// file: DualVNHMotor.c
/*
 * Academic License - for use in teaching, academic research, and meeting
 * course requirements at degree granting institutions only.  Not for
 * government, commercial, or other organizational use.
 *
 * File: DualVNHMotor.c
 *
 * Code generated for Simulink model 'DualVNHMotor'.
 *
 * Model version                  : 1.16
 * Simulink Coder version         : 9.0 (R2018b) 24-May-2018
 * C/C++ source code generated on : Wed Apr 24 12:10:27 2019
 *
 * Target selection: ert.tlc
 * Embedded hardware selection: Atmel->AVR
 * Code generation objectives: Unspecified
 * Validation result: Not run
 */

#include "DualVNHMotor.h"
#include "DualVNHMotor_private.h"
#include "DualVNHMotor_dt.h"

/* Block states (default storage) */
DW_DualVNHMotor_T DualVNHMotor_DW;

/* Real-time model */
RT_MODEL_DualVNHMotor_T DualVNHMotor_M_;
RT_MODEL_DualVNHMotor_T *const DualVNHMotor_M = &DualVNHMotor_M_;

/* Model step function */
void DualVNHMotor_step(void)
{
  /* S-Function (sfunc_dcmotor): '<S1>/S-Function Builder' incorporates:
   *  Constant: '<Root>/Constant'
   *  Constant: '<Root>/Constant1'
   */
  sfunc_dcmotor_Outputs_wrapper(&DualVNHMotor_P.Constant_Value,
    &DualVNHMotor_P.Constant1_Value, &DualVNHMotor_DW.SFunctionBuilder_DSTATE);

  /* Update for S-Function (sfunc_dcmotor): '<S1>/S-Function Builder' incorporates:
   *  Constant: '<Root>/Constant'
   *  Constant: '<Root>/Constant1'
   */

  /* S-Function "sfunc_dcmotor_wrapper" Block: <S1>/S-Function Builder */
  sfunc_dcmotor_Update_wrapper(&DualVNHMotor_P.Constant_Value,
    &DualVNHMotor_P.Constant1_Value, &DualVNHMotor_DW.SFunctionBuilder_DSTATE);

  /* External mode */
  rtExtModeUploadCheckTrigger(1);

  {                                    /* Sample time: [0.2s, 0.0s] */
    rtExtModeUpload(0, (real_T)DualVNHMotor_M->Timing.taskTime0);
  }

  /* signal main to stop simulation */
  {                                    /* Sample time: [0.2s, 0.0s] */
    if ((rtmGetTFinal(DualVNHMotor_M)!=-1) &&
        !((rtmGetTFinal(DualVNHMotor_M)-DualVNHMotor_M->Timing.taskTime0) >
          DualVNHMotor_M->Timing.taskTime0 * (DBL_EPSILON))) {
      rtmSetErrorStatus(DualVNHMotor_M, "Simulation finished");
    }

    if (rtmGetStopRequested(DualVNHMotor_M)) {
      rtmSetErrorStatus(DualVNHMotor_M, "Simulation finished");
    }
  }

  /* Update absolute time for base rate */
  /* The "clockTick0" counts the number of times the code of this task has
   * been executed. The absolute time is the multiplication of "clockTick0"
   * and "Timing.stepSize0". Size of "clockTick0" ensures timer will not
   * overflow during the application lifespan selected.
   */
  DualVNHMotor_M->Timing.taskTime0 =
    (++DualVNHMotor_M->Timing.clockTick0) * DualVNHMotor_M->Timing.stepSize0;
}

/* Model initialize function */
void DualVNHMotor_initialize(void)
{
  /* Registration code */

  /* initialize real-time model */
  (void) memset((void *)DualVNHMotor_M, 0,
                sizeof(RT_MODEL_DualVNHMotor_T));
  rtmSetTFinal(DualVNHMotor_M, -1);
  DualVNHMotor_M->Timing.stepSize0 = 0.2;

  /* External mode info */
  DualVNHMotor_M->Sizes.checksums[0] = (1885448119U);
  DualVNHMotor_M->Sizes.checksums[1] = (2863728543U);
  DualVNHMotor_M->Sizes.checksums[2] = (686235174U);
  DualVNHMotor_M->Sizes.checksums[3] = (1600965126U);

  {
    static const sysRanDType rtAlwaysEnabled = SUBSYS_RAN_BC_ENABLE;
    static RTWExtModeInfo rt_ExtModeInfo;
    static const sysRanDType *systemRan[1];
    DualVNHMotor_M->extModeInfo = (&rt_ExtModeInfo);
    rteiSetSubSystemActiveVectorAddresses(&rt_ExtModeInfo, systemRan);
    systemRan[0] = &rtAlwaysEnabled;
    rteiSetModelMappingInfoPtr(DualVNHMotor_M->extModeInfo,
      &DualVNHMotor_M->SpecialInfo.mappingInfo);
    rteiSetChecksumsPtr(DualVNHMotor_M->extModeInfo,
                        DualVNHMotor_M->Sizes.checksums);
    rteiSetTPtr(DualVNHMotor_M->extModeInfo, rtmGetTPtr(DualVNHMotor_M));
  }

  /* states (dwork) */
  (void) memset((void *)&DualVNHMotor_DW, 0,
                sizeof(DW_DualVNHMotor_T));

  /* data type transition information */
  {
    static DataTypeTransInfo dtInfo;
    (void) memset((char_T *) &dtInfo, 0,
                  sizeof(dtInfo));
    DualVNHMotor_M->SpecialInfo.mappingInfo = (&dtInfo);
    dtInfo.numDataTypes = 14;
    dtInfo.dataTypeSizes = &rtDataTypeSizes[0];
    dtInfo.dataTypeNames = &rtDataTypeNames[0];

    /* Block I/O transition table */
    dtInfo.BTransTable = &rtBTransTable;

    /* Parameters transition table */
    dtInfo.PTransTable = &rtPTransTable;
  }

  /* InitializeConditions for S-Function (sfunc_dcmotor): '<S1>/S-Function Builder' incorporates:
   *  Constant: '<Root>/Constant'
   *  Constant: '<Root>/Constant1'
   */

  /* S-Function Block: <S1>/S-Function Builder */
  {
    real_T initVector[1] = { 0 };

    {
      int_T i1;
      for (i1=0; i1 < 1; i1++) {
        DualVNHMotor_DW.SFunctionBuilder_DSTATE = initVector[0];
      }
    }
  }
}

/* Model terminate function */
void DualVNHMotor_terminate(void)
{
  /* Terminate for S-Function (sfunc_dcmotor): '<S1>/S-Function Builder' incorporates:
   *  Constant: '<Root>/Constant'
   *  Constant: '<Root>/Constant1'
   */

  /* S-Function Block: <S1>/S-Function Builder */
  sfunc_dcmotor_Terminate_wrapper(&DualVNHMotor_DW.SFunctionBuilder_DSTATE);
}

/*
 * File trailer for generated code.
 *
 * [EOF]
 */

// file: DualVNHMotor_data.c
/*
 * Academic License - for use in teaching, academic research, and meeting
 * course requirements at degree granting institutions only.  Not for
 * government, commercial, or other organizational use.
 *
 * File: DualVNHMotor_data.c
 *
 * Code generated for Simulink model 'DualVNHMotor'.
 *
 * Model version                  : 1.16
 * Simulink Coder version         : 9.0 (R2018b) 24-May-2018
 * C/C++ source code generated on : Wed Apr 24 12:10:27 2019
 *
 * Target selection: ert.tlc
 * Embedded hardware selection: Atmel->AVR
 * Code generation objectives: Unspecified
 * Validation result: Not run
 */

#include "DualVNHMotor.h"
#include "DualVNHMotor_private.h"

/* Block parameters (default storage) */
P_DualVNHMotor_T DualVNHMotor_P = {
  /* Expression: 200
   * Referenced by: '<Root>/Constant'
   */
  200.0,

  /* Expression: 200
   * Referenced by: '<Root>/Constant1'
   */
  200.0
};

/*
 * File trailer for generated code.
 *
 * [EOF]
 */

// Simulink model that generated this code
simulink model "DualVNHMotor"  (R2018b)
settings: Solver=FixedStepAuto  StartTime=0.0  StopTime=inf  RelTol=1e-3  EnableMultiTasking=on

== system DualVNHMotor ==
  Constant : Constant
  Constant1 : Constant  Value=200
  Subsystem : Subsystem
  wires:
  Constant/1 -> Subsystem/1(In1)
  Constant1/1 -> Subsystem/2(In2)

== system DualVNHMotor/Subsystem ==
  In1 : Inport
  In2 : Inport  Port=2
  S-Function Builder : S-Function  InitFcn=try, set_param(gcb,'FunctionName','sfunc_dcmotor'), end  FunctionName=sfunc_dcmotor  SFunctionModules=sfunc_dcmotor_wrapper  SFunctionDeploymentMode=off  EnableBusSupport=off  mask(S-Function Builder){}
      mask help: Simulink:masks:SFunctionBuilder_MD
      mask init:
      | val = [[.9  0.75 0.75 1 1 .9 .9 1]',[1 1 0.75 0.75 .9 .9 1 .9]'];try , sys = get_param(gcb,'SfunBuilderFcnName');if isempty(sys), sys = get_param(gcb,'FunctionName'); end,catch, sys = get_param(gcb,'FunctionName'); end
  wires:
  In1/1 -> S-Function Builder/1
  In2/1 -> S-Function Builder/2
